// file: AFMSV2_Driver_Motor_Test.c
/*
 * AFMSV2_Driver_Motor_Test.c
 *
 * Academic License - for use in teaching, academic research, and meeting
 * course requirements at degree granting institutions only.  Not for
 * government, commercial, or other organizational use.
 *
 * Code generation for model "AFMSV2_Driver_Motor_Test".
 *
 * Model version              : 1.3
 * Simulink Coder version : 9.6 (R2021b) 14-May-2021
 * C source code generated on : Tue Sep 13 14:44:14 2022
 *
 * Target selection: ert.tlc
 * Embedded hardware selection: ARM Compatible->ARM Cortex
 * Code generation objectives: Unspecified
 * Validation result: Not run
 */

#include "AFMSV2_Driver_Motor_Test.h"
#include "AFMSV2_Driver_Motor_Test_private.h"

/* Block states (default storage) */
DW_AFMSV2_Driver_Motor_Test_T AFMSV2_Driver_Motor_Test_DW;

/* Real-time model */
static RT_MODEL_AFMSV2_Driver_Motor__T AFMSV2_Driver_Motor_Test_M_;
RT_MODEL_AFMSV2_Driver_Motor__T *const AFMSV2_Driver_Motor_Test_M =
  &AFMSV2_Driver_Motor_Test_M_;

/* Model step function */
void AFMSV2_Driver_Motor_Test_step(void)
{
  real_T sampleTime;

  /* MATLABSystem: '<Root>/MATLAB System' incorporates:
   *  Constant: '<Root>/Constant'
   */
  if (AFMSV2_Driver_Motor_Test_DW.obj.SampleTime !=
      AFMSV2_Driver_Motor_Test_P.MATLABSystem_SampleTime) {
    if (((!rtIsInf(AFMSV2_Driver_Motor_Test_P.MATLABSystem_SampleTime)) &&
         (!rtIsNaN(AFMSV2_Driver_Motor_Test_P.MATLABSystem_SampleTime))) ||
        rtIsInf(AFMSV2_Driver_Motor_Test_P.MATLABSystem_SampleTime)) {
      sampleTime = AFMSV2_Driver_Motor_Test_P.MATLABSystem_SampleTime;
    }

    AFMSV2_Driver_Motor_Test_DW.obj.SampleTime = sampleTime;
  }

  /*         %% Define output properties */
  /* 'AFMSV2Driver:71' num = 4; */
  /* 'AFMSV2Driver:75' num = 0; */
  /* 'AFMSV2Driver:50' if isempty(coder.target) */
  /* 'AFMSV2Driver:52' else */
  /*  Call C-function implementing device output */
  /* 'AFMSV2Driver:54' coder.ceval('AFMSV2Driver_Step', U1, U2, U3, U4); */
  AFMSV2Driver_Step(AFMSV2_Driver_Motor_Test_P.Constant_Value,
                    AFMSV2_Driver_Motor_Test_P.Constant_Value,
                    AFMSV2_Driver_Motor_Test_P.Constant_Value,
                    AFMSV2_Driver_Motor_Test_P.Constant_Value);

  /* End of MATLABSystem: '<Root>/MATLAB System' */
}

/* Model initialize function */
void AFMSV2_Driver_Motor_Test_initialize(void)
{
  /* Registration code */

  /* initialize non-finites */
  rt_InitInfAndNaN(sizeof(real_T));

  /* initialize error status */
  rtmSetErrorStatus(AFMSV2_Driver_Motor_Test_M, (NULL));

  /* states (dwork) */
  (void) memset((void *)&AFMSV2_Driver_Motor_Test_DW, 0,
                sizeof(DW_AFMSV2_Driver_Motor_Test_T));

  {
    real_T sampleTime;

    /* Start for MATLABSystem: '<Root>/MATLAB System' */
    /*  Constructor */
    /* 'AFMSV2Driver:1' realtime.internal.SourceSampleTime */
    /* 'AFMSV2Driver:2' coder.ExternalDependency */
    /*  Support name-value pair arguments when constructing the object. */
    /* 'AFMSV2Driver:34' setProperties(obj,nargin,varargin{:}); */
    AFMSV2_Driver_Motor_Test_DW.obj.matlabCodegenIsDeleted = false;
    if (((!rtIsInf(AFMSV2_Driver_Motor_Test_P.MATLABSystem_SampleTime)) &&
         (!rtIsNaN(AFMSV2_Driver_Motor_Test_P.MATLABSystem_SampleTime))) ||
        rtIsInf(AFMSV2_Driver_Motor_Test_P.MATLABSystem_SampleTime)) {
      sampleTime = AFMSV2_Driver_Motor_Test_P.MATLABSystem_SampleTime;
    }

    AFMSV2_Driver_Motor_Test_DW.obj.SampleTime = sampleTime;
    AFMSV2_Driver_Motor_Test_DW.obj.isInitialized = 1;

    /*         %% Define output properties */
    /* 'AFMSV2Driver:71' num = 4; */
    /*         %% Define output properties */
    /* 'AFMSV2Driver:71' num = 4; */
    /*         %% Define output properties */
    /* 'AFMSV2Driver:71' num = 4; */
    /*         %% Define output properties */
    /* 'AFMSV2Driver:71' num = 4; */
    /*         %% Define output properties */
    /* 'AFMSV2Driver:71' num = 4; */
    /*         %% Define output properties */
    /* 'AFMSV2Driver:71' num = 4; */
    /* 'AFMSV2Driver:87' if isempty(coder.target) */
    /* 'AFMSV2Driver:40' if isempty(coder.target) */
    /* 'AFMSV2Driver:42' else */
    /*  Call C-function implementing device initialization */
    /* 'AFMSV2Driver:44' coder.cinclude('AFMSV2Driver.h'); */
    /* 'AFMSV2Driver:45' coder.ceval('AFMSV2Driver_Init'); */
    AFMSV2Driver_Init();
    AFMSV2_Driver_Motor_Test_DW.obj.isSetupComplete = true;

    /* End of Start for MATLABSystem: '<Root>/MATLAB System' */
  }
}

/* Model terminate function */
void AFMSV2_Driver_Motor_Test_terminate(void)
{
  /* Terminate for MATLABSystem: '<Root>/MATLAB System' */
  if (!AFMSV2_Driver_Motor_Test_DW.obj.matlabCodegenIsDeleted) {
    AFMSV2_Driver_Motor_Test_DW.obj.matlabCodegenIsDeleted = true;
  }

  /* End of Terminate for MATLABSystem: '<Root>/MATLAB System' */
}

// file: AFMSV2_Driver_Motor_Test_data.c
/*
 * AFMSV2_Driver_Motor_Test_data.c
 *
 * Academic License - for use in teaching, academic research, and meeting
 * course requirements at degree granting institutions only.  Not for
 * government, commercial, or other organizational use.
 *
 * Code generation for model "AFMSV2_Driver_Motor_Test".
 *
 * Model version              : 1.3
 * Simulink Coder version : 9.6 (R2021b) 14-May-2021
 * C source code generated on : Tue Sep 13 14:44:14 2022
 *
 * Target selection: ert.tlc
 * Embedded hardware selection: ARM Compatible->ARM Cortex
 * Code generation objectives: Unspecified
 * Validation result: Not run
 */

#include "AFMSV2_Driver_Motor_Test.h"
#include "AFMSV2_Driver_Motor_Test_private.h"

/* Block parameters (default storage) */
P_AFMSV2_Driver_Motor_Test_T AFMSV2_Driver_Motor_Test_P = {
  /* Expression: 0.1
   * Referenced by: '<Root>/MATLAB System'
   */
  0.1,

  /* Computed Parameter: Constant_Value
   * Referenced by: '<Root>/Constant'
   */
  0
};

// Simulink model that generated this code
simulink model "AFMSV2_Driver_Motor_Test"  (R2021b)
settings: Solver=ode3  StartTime=0.0  StopTime=inf  RelTol=1e-3  EnableMultiTasking=on

== system AFMSV2_Driver_Motor_Test ==
  Constant : Constant  Value=0
  MATLAB System : MATLABSystem  System=AFMSV2Driver  SampleTime=0.1
  wires:
  Constant/1 -> MATLAB System/4, MATLAB System/3, MATLAB System/2, MATLAB System/1
